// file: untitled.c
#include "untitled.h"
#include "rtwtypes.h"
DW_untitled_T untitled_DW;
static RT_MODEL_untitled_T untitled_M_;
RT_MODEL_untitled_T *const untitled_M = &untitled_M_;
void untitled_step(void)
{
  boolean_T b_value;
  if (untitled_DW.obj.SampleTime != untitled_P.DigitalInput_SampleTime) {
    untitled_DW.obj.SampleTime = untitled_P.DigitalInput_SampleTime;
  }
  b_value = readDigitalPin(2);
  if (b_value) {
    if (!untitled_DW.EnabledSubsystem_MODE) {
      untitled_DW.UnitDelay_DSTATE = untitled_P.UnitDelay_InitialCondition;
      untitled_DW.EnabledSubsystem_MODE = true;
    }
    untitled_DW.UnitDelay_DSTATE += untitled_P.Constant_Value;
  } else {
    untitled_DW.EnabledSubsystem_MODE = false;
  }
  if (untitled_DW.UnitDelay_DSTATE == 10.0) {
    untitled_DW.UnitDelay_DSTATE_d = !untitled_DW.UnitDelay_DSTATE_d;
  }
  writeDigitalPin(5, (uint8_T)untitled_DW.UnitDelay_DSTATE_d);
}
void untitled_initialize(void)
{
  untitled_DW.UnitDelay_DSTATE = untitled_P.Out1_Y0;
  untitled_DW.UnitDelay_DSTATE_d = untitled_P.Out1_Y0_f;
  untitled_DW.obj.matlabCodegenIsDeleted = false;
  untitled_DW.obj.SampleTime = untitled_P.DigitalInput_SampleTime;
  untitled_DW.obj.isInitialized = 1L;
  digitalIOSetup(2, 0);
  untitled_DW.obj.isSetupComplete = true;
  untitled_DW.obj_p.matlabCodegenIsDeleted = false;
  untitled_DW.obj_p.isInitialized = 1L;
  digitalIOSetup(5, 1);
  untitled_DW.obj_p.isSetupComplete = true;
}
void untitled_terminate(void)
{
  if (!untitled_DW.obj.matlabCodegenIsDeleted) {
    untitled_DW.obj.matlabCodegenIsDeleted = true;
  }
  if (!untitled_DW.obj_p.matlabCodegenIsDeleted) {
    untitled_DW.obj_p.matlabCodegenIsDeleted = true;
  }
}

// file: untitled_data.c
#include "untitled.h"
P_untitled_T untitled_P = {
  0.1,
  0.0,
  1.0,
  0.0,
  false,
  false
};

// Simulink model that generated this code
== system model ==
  DigitalOutput#1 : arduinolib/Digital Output  pinNumber=5  <- 1: Subsystem#1
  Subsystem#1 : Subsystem  <- Action: If#1
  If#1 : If  IfExpression=u1 == 10  <- 1: EnabledSubsystem
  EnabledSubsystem : Subsystem  <- Enable: DigitalInput
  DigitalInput : arduinolib/Digital Input  pinNumber=2
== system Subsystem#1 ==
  ActionPort#1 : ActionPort
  Out1 : Outport  <- 1: Logic#1
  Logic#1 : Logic  Operator=NOT  <- 1: UnitDelay
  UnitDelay : UnitDelay  <- 1: Logic#1
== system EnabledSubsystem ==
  EnablePort#1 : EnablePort
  Outport#1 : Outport  <- 1: Sum#1
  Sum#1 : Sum  <- 1: Constant, 2: UnitDelay#1
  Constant : Constant
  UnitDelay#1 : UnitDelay  <- 1: Sum#1
